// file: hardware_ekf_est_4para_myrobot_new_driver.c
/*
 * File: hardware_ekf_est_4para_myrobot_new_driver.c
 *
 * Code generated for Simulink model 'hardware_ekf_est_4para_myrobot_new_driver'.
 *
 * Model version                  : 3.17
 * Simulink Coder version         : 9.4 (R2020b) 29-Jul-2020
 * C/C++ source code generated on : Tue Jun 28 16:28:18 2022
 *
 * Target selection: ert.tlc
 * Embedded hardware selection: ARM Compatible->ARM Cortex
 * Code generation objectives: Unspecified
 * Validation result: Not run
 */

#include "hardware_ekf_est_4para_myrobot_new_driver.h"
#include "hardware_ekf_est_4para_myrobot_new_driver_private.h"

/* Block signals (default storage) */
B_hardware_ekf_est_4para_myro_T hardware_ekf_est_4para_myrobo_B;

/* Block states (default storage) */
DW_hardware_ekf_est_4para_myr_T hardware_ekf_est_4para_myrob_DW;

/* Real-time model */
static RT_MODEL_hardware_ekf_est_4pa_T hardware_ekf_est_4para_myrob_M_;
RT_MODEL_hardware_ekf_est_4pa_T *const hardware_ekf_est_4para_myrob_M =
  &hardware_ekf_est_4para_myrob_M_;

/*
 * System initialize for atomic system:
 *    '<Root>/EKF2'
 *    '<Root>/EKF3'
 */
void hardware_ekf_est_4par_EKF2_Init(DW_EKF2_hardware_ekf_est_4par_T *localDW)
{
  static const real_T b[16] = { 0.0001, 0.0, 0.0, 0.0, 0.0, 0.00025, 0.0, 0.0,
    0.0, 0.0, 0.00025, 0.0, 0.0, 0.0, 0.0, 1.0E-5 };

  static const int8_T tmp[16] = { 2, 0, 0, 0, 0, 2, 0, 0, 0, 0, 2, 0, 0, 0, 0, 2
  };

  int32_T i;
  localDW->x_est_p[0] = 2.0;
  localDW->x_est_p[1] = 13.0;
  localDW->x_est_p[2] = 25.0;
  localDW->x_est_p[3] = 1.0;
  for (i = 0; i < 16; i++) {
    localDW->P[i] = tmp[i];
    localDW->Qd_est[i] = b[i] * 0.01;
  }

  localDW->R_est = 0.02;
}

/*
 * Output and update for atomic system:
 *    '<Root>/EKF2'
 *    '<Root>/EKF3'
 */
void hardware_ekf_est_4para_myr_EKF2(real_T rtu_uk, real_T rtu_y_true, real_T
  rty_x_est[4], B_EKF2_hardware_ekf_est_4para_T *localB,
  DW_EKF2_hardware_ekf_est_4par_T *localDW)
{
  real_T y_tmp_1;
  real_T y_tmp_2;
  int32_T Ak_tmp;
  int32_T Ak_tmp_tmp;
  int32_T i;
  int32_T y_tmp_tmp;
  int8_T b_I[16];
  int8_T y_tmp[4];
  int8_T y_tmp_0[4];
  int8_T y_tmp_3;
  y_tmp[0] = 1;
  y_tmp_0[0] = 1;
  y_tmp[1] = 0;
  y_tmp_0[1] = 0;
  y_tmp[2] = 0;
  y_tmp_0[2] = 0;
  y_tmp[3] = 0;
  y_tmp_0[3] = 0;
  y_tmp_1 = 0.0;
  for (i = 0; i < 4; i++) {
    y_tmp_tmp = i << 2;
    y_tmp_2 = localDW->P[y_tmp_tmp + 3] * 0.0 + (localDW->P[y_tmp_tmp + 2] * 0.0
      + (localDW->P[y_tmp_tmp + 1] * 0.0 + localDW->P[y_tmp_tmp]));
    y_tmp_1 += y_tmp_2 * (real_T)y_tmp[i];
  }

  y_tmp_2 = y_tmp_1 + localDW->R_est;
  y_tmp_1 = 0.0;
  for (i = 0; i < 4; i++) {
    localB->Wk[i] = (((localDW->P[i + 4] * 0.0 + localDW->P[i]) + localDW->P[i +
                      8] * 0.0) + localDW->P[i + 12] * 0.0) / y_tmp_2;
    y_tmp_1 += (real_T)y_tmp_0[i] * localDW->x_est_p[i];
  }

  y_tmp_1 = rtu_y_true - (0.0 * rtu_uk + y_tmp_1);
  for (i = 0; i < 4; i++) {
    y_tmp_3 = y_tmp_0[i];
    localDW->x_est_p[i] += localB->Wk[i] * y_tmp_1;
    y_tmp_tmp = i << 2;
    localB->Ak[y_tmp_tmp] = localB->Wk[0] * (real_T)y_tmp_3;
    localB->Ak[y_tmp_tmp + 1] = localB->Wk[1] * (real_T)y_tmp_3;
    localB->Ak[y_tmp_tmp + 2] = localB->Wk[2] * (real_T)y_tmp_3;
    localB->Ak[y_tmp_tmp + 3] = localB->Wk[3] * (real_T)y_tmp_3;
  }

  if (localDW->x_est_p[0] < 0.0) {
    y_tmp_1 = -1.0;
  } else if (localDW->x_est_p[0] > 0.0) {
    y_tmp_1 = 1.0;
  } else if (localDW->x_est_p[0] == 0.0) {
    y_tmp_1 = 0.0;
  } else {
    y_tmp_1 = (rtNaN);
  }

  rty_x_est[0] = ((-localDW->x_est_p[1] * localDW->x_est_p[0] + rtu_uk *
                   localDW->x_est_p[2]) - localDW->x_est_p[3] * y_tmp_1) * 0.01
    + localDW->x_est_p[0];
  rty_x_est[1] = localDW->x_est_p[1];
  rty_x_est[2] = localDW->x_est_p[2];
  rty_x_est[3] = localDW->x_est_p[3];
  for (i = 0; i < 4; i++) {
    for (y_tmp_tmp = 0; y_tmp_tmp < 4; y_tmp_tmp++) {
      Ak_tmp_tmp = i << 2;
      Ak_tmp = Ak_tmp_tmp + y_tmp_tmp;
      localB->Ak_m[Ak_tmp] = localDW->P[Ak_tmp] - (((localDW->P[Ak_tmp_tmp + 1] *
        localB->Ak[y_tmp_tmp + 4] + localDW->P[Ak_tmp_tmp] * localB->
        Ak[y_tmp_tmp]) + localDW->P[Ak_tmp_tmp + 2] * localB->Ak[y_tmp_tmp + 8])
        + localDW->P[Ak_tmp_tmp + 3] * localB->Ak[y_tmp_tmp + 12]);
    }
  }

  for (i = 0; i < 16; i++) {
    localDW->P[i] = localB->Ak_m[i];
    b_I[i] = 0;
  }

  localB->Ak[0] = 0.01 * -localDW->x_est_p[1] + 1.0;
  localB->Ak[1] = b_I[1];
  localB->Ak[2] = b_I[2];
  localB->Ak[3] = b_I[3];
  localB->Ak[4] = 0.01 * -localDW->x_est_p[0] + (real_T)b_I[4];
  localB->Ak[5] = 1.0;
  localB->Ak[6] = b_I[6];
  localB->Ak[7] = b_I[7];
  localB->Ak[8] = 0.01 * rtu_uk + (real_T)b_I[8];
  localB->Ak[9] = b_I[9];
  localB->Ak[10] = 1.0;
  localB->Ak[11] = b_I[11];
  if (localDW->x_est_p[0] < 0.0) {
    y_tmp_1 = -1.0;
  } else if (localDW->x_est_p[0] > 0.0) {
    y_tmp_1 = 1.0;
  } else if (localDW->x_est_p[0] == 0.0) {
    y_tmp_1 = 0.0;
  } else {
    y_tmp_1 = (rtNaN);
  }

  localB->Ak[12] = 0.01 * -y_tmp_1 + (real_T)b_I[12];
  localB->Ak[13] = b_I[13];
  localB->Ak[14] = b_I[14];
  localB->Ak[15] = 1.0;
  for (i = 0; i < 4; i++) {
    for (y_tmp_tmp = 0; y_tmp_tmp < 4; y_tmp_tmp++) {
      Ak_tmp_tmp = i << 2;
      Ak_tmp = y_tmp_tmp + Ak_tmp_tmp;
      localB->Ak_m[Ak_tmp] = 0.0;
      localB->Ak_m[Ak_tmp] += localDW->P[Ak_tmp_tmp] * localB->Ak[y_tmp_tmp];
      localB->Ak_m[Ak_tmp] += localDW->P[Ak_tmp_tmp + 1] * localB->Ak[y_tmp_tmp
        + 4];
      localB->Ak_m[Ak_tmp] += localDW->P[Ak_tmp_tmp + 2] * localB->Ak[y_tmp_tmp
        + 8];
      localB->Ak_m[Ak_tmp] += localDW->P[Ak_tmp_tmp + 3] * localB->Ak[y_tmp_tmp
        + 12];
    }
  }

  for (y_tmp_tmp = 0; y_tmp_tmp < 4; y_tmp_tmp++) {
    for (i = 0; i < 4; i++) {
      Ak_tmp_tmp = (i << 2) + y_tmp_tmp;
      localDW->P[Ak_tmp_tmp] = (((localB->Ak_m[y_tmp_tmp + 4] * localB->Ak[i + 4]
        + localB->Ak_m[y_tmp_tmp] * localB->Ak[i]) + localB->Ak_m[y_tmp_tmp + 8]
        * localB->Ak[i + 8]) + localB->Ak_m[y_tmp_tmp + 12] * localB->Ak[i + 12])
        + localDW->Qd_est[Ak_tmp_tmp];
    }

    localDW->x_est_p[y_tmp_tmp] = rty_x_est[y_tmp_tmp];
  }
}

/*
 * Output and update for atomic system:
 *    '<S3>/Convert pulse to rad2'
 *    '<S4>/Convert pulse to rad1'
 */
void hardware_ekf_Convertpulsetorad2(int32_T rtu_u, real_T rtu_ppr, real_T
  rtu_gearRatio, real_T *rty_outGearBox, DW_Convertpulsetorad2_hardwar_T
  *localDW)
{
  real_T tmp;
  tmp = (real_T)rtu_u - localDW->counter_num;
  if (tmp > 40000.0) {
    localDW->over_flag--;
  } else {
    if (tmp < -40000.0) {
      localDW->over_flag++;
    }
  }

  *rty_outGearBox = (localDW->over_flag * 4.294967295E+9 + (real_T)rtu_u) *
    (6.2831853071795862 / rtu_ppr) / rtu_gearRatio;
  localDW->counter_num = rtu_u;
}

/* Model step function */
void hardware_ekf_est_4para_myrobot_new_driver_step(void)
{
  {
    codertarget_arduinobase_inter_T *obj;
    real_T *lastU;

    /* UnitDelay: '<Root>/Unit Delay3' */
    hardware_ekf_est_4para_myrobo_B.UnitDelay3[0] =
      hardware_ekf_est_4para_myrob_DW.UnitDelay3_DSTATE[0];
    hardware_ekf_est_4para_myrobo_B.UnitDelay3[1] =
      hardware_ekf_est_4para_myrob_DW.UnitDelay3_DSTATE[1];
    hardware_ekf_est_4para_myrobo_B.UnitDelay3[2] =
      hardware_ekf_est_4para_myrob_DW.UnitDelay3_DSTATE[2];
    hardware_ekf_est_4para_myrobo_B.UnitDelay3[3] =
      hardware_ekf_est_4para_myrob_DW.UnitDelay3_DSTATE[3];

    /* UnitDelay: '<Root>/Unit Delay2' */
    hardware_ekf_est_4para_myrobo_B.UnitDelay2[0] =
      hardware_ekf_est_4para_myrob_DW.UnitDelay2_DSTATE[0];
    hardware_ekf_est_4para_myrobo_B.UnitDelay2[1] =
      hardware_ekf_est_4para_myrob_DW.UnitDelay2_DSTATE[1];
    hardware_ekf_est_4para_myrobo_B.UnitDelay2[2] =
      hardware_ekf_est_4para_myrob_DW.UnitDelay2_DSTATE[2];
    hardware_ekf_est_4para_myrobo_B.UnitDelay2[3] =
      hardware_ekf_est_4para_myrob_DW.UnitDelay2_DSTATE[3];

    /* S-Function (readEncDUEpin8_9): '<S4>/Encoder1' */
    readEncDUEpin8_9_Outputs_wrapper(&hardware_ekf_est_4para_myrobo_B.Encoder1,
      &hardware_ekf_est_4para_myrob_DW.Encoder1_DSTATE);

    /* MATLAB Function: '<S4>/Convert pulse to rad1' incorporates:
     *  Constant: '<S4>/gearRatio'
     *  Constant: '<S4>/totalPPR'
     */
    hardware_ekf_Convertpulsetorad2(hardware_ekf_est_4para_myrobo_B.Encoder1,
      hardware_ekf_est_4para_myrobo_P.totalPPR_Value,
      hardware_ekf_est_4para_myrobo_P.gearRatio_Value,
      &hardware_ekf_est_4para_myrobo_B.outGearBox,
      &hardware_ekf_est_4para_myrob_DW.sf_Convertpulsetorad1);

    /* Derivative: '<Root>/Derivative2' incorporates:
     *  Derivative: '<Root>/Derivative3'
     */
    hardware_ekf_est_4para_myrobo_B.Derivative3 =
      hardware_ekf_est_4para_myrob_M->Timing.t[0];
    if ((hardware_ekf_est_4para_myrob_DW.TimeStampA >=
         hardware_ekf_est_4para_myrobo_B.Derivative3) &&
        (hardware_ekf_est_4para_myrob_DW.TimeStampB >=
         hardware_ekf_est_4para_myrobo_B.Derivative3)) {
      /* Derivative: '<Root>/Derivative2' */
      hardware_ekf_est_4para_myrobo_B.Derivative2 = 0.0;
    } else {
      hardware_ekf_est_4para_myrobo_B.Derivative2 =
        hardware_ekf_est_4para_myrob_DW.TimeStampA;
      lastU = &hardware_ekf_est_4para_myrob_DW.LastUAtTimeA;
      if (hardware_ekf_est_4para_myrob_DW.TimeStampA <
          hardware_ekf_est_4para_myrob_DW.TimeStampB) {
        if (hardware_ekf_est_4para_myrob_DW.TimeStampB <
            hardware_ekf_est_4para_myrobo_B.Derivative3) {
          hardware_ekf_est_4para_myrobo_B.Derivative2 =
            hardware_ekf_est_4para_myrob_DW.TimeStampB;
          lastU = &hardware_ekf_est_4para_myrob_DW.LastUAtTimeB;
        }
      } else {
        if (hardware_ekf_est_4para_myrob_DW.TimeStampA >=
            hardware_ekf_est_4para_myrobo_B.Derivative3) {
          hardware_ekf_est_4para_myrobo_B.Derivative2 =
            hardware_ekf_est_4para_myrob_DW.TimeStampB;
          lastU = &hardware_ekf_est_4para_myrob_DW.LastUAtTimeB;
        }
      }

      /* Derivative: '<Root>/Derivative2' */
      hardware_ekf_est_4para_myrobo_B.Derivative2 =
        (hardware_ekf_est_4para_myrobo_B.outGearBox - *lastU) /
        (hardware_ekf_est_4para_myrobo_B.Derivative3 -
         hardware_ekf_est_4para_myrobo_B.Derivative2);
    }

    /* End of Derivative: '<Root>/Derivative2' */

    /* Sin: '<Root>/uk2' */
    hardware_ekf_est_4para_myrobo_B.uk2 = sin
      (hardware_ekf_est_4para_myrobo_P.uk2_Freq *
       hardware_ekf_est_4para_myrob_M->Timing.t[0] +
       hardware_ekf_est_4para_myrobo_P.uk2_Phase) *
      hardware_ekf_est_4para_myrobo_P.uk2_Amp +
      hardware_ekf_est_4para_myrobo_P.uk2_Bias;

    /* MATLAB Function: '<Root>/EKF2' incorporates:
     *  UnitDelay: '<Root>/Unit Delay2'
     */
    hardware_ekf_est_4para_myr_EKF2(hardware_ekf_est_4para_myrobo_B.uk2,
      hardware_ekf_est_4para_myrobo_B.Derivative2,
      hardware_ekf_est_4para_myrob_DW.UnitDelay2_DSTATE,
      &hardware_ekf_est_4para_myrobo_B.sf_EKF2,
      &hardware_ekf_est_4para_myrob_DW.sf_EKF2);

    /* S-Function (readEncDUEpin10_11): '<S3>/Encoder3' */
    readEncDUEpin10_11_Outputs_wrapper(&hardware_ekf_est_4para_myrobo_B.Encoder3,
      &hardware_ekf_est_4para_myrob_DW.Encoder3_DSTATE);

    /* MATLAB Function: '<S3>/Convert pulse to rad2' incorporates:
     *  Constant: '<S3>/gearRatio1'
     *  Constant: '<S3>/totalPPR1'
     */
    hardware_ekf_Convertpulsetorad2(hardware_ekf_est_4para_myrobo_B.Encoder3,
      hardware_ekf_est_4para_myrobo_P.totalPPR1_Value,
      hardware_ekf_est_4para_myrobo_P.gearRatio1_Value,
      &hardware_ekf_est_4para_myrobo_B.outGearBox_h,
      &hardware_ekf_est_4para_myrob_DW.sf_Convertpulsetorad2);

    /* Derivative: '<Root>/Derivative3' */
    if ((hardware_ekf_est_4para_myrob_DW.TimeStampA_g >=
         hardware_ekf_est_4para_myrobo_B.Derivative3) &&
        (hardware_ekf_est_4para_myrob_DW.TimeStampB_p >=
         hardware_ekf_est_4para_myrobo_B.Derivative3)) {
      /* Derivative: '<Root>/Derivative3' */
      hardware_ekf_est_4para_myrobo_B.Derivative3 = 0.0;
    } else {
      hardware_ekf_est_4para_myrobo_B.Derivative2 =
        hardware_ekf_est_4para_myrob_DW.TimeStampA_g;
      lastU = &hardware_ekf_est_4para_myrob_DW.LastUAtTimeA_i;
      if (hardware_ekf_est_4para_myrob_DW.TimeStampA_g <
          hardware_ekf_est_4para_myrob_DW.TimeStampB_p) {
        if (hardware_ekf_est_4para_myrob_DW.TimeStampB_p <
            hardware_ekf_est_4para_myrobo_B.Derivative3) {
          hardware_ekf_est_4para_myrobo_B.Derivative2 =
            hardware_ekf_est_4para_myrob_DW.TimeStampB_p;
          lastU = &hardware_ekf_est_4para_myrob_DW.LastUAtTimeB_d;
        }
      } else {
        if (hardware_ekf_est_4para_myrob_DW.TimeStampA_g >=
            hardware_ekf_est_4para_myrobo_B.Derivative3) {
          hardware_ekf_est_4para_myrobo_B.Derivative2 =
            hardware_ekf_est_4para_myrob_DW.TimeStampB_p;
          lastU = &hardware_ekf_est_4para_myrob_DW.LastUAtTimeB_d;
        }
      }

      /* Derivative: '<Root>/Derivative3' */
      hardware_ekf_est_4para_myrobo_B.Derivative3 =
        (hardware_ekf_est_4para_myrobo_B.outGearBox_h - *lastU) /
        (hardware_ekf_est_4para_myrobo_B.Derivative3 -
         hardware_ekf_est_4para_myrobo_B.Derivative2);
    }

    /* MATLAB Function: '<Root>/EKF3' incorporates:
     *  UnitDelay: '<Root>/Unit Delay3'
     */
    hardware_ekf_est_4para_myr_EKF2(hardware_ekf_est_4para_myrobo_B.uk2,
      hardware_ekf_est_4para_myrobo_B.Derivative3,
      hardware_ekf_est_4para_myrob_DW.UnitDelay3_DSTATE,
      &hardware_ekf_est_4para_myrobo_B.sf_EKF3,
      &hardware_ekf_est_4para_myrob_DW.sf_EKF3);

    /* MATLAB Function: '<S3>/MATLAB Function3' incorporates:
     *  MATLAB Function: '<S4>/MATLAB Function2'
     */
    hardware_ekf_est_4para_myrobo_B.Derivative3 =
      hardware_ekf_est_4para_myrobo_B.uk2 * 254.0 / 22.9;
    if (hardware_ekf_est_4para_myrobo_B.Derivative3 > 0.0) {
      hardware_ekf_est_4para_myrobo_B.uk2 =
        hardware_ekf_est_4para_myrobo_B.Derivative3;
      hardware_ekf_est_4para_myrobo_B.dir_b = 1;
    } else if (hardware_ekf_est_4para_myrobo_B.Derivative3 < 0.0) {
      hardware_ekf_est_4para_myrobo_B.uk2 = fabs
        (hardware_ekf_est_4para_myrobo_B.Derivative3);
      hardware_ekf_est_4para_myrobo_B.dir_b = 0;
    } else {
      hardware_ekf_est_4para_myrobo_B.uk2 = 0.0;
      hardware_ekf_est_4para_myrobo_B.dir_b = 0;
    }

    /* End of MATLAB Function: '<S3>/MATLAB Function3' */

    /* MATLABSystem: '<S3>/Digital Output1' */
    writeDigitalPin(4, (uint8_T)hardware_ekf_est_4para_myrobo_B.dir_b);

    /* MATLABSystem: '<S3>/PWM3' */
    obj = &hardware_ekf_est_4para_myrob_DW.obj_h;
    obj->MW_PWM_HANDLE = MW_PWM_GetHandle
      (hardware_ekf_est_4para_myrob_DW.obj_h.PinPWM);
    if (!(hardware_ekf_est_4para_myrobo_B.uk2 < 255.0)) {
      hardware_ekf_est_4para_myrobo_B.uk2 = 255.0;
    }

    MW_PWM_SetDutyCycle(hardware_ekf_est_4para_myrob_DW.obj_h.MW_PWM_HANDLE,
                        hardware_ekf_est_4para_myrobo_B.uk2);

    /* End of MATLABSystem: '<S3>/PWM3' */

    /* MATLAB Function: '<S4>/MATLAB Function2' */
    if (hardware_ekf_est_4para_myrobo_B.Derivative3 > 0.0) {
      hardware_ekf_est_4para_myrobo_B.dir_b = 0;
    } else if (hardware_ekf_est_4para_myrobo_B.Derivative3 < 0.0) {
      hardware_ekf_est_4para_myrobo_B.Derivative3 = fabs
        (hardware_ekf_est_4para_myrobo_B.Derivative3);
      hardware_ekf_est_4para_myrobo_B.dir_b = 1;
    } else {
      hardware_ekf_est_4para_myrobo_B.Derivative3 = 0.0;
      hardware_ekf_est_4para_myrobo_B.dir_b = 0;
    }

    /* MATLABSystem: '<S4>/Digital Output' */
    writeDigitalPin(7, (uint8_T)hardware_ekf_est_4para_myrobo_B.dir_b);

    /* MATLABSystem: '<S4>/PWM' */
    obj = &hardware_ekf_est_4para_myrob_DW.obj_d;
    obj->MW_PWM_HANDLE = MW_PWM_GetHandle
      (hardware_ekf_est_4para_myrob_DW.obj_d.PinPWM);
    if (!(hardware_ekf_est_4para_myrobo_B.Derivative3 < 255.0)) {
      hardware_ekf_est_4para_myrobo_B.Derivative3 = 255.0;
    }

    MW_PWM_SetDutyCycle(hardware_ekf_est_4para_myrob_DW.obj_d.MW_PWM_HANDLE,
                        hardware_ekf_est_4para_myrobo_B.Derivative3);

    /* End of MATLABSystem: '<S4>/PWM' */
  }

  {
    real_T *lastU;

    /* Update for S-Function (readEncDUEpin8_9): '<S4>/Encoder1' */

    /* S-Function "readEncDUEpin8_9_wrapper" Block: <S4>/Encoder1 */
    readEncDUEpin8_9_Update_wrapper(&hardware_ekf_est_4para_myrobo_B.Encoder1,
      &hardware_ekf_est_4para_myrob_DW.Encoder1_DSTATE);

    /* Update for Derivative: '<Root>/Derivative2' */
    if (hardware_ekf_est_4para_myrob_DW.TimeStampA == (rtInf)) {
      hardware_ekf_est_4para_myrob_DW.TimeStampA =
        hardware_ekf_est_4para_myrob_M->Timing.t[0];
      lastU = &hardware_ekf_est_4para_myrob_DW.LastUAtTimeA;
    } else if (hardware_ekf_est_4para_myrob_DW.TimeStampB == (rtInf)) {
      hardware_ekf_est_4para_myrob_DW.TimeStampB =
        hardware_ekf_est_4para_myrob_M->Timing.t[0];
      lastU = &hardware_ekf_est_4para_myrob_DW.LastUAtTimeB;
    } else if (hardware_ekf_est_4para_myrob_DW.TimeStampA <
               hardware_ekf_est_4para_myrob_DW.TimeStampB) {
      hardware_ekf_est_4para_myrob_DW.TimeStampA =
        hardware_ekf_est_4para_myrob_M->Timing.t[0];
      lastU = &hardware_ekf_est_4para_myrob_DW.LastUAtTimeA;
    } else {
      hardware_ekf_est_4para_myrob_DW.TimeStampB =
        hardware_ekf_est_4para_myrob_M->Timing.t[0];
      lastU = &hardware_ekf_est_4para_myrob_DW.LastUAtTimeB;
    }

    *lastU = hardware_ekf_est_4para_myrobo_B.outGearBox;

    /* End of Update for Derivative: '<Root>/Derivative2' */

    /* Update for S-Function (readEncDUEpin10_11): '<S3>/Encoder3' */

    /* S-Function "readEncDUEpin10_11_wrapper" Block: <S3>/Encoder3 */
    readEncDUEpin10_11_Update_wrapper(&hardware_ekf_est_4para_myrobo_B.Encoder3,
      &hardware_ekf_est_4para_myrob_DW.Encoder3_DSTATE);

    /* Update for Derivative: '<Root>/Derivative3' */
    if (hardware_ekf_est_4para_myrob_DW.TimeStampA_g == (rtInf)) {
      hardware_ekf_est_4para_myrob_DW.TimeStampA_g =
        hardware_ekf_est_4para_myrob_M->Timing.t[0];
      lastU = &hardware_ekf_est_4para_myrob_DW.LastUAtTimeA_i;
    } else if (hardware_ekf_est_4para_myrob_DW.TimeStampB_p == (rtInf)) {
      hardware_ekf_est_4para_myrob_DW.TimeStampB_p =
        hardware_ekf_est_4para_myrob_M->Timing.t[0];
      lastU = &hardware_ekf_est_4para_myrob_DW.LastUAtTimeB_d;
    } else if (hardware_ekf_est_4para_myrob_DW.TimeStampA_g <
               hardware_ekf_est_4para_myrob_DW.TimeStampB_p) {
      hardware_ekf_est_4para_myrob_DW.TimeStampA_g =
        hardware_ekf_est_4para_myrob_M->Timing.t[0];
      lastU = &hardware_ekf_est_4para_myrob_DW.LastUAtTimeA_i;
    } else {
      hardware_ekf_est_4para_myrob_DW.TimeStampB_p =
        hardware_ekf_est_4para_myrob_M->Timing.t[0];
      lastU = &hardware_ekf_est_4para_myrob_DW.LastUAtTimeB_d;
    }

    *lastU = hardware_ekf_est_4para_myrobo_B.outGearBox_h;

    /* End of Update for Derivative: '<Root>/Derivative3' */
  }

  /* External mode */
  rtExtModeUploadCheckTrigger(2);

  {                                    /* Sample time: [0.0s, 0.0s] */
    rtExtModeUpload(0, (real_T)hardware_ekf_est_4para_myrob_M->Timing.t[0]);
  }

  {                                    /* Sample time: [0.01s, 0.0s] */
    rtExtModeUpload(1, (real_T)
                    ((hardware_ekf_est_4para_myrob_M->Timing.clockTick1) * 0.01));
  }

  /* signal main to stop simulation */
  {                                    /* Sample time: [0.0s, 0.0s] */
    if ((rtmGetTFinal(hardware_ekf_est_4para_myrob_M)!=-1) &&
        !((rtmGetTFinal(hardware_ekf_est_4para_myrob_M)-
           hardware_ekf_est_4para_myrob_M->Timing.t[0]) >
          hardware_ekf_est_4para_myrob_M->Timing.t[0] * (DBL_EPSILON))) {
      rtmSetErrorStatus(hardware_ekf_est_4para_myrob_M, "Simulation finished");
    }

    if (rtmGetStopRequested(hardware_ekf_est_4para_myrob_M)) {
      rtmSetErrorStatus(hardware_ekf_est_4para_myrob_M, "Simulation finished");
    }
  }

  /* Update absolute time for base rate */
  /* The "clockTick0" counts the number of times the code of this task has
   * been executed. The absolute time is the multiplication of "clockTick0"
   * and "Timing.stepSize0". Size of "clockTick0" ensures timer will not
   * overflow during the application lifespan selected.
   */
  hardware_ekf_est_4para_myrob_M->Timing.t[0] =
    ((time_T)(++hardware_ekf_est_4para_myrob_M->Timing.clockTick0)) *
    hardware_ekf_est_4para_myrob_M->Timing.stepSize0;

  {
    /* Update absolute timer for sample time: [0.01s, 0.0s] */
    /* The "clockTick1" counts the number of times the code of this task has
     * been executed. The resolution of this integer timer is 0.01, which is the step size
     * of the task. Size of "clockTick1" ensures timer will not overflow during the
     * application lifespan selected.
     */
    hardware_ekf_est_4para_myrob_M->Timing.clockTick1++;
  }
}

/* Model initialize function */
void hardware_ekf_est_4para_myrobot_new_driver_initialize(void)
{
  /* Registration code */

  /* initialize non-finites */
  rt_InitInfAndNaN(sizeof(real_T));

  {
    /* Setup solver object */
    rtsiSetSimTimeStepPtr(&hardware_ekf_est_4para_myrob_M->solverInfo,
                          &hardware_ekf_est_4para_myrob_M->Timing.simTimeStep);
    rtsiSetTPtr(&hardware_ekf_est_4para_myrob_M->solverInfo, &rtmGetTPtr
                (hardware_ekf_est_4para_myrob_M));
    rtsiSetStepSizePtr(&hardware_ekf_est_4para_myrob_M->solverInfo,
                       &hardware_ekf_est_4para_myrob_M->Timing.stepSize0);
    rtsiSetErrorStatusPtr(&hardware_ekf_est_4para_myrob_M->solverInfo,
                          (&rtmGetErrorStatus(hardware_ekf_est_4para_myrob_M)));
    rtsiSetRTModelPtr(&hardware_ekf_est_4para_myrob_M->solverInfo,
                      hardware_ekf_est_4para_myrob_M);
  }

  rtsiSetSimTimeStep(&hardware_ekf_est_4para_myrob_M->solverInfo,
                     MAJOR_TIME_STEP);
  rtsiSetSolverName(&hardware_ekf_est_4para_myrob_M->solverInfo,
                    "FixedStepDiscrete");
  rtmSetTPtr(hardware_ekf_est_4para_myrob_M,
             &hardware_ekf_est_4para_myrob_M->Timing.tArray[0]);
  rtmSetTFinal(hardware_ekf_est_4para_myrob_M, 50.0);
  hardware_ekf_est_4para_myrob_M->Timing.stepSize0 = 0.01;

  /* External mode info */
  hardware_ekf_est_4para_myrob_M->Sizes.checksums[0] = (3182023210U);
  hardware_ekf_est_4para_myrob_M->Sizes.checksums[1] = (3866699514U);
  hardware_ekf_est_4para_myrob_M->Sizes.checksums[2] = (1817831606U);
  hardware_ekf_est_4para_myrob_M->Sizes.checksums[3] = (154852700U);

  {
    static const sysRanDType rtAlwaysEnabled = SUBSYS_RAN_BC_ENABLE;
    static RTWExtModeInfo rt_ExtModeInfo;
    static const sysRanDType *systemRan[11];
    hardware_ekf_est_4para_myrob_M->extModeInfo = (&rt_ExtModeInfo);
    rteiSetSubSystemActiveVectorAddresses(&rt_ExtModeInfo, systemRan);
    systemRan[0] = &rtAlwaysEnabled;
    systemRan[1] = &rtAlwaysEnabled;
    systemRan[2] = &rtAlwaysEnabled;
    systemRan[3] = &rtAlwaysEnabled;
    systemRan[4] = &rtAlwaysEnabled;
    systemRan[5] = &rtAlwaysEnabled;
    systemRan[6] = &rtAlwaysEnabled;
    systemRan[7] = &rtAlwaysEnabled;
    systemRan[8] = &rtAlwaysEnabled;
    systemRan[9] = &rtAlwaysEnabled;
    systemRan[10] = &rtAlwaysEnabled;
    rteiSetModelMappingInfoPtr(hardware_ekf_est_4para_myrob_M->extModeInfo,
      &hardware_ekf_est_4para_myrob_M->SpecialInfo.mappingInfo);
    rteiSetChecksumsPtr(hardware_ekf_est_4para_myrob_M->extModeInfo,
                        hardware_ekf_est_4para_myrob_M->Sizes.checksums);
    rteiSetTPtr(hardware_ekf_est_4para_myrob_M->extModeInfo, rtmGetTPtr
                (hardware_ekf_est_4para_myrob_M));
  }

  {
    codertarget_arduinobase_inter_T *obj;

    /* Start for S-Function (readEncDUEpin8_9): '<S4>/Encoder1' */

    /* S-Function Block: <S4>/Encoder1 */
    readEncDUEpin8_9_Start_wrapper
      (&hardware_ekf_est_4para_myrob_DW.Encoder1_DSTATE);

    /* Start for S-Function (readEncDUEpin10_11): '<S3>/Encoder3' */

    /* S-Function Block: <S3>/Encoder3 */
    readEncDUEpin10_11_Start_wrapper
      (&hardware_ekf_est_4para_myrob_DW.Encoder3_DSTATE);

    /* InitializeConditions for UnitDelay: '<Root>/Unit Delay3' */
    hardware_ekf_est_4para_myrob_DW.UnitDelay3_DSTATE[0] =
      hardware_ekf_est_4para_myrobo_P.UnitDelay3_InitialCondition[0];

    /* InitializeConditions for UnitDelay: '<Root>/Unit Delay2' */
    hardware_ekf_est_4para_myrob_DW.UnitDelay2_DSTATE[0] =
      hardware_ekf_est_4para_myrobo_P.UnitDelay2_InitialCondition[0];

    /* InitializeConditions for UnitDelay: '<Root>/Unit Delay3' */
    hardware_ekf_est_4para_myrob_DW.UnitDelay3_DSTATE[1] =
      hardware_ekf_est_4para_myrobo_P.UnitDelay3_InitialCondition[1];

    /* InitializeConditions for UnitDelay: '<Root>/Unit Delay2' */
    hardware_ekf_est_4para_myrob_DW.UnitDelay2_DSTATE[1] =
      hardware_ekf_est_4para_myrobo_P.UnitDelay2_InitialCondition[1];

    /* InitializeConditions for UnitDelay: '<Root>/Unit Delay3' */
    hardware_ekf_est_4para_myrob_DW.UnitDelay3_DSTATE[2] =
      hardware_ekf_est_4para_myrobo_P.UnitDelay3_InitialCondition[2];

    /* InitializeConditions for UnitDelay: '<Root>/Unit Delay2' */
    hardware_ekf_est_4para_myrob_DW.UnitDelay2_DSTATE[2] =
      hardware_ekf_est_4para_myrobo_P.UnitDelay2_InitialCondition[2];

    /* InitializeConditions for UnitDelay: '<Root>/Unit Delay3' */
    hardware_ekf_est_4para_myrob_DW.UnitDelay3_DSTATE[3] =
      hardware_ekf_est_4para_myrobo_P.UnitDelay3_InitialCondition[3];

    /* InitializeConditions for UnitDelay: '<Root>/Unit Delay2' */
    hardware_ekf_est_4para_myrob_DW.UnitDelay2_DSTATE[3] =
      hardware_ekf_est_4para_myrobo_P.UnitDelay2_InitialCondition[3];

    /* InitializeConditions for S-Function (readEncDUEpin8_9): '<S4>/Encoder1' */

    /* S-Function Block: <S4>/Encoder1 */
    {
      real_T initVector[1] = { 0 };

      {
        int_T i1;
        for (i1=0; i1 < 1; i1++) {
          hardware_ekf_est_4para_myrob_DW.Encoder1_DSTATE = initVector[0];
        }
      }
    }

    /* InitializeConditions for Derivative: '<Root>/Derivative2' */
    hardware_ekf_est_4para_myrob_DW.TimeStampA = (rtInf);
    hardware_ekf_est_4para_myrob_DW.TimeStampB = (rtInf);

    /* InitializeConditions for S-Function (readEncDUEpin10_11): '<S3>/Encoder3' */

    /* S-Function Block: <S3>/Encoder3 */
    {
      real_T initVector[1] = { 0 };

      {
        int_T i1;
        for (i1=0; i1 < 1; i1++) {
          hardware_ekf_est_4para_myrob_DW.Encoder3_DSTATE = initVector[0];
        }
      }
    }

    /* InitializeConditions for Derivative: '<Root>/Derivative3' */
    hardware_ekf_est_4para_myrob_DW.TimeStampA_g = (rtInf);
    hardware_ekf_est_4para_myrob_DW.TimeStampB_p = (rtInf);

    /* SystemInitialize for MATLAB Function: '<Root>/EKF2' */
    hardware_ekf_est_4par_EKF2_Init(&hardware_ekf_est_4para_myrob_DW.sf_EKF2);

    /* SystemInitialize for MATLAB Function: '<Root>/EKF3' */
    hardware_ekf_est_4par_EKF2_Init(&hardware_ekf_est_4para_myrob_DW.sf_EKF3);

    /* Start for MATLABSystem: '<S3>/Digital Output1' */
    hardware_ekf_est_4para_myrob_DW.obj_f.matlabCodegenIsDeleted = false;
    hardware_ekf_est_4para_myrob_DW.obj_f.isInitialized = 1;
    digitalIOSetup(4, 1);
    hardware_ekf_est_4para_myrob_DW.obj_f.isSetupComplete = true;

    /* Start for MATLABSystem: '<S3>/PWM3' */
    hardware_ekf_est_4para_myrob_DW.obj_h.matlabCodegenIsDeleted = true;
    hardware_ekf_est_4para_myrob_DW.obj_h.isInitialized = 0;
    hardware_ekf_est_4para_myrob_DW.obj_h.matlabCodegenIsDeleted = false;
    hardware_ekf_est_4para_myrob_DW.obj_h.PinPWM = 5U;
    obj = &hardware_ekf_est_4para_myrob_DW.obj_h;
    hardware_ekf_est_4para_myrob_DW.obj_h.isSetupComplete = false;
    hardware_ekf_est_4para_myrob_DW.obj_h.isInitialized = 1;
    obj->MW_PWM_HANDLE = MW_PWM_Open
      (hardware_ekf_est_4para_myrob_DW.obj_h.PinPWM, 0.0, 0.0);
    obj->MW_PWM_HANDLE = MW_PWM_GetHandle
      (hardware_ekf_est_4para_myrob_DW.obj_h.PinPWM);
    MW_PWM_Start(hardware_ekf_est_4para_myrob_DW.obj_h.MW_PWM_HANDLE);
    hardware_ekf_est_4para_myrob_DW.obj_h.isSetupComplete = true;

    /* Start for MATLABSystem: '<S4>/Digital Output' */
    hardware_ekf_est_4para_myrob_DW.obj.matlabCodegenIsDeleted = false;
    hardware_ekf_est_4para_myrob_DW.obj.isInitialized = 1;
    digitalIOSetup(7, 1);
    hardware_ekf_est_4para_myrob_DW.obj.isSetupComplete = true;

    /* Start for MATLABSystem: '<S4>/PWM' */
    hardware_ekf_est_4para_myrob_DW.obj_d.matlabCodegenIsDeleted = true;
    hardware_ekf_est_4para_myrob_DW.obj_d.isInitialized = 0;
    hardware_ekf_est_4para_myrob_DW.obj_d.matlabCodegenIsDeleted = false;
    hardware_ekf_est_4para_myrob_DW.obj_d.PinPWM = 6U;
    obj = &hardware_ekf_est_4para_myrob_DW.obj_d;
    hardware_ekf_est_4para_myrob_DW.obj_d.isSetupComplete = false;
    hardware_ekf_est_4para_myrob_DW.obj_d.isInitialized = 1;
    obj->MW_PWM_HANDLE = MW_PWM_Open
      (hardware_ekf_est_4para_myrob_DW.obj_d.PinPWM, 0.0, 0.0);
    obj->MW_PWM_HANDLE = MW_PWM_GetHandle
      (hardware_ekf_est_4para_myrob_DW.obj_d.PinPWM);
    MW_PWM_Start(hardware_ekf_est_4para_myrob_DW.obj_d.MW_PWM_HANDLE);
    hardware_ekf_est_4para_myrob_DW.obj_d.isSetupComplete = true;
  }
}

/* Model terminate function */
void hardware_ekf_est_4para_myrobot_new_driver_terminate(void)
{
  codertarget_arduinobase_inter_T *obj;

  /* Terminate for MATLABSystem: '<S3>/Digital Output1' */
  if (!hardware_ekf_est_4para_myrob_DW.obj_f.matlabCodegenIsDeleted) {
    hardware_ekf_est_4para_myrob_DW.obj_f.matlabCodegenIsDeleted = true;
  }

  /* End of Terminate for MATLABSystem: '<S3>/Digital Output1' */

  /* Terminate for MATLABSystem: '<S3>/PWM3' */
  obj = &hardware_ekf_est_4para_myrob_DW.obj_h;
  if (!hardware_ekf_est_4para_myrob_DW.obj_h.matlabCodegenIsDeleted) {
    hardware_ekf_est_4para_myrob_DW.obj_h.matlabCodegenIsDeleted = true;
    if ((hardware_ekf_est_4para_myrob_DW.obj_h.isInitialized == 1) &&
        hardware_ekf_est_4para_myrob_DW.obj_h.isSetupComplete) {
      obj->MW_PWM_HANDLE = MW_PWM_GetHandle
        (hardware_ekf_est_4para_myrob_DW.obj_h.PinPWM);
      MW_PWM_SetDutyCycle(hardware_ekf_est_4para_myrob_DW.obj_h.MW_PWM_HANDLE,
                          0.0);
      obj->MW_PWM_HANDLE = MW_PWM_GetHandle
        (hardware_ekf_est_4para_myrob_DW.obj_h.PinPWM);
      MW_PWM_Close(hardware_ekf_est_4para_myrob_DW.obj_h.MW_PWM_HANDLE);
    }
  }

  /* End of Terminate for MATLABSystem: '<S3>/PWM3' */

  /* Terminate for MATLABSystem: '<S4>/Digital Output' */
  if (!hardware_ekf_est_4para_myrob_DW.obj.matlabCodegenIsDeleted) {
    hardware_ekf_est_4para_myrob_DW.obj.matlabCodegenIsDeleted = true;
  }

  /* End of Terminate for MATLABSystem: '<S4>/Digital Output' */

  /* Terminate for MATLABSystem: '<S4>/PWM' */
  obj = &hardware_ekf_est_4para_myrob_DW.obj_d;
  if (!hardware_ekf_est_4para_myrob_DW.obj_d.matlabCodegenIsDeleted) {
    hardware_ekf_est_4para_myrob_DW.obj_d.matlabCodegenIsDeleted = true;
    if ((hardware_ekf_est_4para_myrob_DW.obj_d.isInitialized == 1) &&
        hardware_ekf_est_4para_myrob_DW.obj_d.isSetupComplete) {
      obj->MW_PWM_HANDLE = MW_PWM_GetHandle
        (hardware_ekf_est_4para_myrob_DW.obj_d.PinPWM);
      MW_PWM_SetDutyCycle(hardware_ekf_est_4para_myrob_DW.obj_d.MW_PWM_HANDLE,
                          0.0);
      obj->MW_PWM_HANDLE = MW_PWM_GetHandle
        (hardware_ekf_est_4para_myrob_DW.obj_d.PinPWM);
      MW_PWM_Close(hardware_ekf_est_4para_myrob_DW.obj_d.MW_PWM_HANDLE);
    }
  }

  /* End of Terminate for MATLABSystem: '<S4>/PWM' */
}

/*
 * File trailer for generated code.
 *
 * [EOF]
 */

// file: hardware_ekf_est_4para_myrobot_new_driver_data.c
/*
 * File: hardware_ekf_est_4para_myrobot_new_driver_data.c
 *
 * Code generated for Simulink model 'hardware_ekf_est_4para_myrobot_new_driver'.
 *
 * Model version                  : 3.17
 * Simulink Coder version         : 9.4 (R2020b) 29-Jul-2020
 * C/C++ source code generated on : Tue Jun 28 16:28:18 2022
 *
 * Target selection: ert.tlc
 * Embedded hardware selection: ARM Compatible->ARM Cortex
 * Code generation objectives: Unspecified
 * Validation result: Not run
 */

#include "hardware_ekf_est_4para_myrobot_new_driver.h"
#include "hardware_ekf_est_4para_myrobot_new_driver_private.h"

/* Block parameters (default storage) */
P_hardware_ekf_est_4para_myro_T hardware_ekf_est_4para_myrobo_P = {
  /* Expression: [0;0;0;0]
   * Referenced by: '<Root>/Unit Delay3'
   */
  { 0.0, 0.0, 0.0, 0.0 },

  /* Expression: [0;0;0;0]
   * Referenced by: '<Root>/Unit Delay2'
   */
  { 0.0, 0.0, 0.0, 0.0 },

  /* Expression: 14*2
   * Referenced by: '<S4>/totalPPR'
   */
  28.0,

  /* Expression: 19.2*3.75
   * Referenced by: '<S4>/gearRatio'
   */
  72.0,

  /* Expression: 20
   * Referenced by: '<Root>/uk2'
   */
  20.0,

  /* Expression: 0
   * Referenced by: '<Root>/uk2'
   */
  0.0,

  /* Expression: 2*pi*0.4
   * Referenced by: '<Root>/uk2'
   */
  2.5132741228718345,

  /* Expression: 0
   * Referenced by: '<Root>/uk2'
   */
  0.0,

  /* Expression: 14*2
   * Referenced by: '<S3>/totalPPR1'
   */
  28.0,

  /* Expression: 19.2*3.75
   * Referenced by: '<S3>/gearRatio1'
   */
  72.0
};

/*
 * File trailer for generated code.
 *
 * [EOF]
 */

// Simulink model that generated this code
simulink model "hardware_ekf_est_4para_myrobot_new_driver"  (R2020b)
settings: Solver=ode1  StartTime=0.0  StopTime=60  FixedStep=0.01  RelTol=1e-3  EnableMultiTasking=on
libraries: arduinolib x4

== system hardware_ekf_est_4para_myrobot_new_driver ==
  Derivative2 : Derivative
  Derivative3 : Derivative
  Display2 : Display
  Display3 : Display
  EKF2 : MATLAB Function  TreatAsAtomicUnit=on
  EKF3 : MATLAB Function  TreatAsAtomicUnit=on
  Left Motor : Subsystem
  Right motor : Subsystem
  Scope2 : Scope
  Scope3 : Scope
  Unit Delay2 : UnitDelay  InitialCondition=[0;0;0;0]  SampleTime=-1  HasFrameUpgradeWarning=on
  Unit Delay3 : UnitDelay  InitialCondition=[0;0;0;0]  SampleTime=-1  HasFrameUpgradeWarning=on
  uk2 : Sin  Amplitude=20  Frequency=2*pi*0.4  SampleTime=0
  wires:
  Right motor/1(outGearBox) -> Derivative2/1
  Derivative2/1 -> EKF2/2(y_true)
  Derivative3/1 -> EKF3/2(y_true)
  uk2/1 -> Left Motor/1(v_a), EKF3/1(uk), EKF2/1(uk), Right motor/1(v_a)
  Left Motor/1(outGearBox) -> Derivative3/1
  EKF2/1(x_est) -> Unit Delay2/1
  EKF3/1(x_est) -> Unit Delay3/1
  Unit Delay3/1 -> Scope2/1, Display2/1
  Unit Delay2/1 -> Display3/1, Scope3/1

== system hardware_ekf_est_4para_myrobot_new_driver/Left Motor ==
  v_a : Inport
  Convert pulse to rad2 : MATLAB Function  TreatAsAtomicUnit=on
  Digital Output1 : arduinolib/Digital Output  pinNumber=4  Direction=output  blockPlatform=arduino
  Encoder3 : S-Function  InitFcn=try, set_param(gcb,'FunctionName','readEncDUEpin10_11'), end  FunctionName=readEncDUEpin10_11  SFunctionModules=readEncDUEpin10_11_wrapper  SFunctionDeploymentMode=off  EnableBusSupport=off  mask(S-Function Builder){}
      mask help: Simulink:masks:SFunctionBuilder_MD
      mask init:
      | val = [[.9  0.75 0.75 1 1 .9 .9 1]',[1 1 0.75 0.75 .9 .9 1 .9]'];try , sys = get_param(gcb,'SfunBuilderFcnName');if isempty(sys), sys = get_param(gcb,'FunctionName'); end,catch, sys = get_param(gcb,'FunctionName'); end
  MATLAB Function3 : MATLAB Function  TreatAsAtomicUnit=on
  PWM3 : arduinolib/PWM  pinNumber=5  frequencyType=Default  desiredFrequency=490.2  achievableFrequency=490.2
  gearRatio1 : Constant  Value=19.2*3.75
  totalPPR1 : Constant  Value=14*2
  outGearBox : Outport
  wires:
  totalPPR1/1 -> Convert pulse to rad2/2(ppr)
  Convert pulse to rad2/1(outGearBox) -> outGearBox/1
  MATLAB Function3/2(dir) -> Digital Output1/1
  MATLAB Function3/1(pwm) -> PWM3/1
  Encoder3/1 -> Convert pulse to rad2/1(u)
  v_a/1 -> MATLAB Function3/1(v_a)
  gearRatio1/1 -> Convert pulse to rad2/3(gearRatio)

== system hardware_ekf_est_4para_myrobot_new_driver/Right motor ==
  v_a : Inport
  Convert pulse to rad1 : MATLAB Function  TreatAsAtomicUnit=on
  Digital Output : arduinolib/Digital Output  pinNumber=7  Direction=output  blockPlatform=arduino
  Encoder1 : S-Function  InitFcn=try, set_param(gcb,'FunctionName','readEncDUEpin8_9'), end  FunctionName=readEncDUEpin8_9  SFunctionModules=readEncDUEpin8_9_wrapper  SFunctionDeploymentMode=off  EnableBusSupport=off  mask(S-Function Builder){}
      mask help: Simulink:masks:SFunctionBuilder_MD
      mask init: same as hardware_ekf_est_4para_myrobot_new_driver/Left Motor/Encoder3
  MATLAB Function2 : MATLAB Function  TreatAsAtomicUnit=on
  PWM : arduinolib/PWM  pinNumber=6  frequencyType=Default  desiredFrequency=490.2  achievableFrequency=490.2
  gearRatio : Constant  Value=19.2*3.75
  totalPPR : Constant  Value=14*2
  outGearBox : Outport
  wires:
  totalPPR/1 -> Convert pulse to rad1/2(ppr)
  v_a/1 -> MATLAB Function2/1(v_a)
  MATLAB Function2/2(dir) -> Digital Output/1
  MATLAB Function2/1(pwm) -> PWM/1
  gearRatio/1 -> Convert pulse to rad1/3(gearRatio)
  Convert pulse to rad1/1(outGearBox) -> outGearBox/1
  Encoder1/1 -> Convert pulse to rad1/1(u)

== matlab function hardware_ekf_est_4para_myrobot_new_driver/Left Motor/Convert pulse to rad2 ==
  settings: updateMethod=DISCRETE
function outGearBox = fcn(u,ppr,gearRatio)

persistent counter_num over_flag
if(isempty(counter_num)), counter_num = 0;end
if(isempty(over_flag)), over_flag = 0;end
pulse2radian = 2*pi/ppr; % 1 pulse = ?? radian

if(double(u) - counter_num > 40000), over_flag = over_flag-1;
elseif(double(u) - counter_num < -40000), over_flag = over_flag+1;
end

inGearBox = (double(u)+over_flag*(2^32 -1))*pulse2radian; 
outGearBox = inGearBox/gearRatio;
counter_num = double(u) ;

== matlab function hardware_ekf_est_4para_myrobot_new_driver/Right motor/MATLAB Function2 ==
function [pwm,dir] = fcn(v_a)

vmax = 22.9;
pwm_cal = v_a*254/vmax;
if pwm_cal > 0
    pwm = pwm_cal;
    dir = 0;
elseif pwm_cal < 0
    pwm = abs(pwm_cal);
    dir = 1;
else
    pwm = 0;
    dir = 0;
end

== matlab function hardware_ekf_est_4para_myrobot_new_driver/Left Motor/MATLAB Function3 ==
function [pwm,dir] = fcn(v_a)

vmax = 22.9;
pwm_cal = v_a*254/vmax;
if pwm_cal > 0
    pwm = pwm_cal;
    dir = 1;
elseif pwm_cal < 0
    pwm = abs(pwm_cal);
    dir = 0;
else
    pwm = 0;
    dir = 0;
end

== matlab function hardware_ekf_est_4para_myrobot_new_driver/EKF2 ==
  settings: updateMethod=DISCRETE
function x_est = fcn(uk,y_true)
Ts=0.01;
persistent x_est_p P Qd_est R_est Qc_est;
if isempty(x_est_p)
          
          x_est_p=[2;13;25;1];
          P=2*eye(4);
         Qc_est=1e-5*diag([10,25,25,1]);
          Qd_est=Qc_est*Ts;
          R_est=0.02;
end
c=[1 0 0 0];D=0;Ck=c;Dk=D;
%Comput Kalman Gain and update predicted value
Wk=P*Ck'/(Ck*P*Ck'+R_est);
y_est=Ck*x_est_p+Dk*uk;
x=x_est_p+Wk.*(y_true-y_est);
%Compute prediction at next time step
x_est=x+Ts*[-x(2)*x(1)+uk*x(3)-x(4)*sign(x(1));0;0;0];
%Update error covariance matrices
P=P-Wk*Ck*P;
%Define Ak
Ak=eye(4)+Ts*[-x(2) -x(1) uk -sign(x(1));0 0 0 0;0 0 0 0;0 0 0 0];
P=Ak*P*Ak'+Qd_est;
x_est_p=x_est;

== matlab function hardware_ekf_est_4para_myrobot_new_driver/EKF3 ==
  settings: updateMethod=DISCRETE
function x_est = fcn(uk,y_true)
Ts=0.01;
persistent x_est_p P Qd_est R_est Qc_est;
if isempty(x_est_p)
          
          x_est_p=[2;13;25;1];
          P=2*eye(4);
         Qc_est=1e-5*diag([10,25,25,1]);
          Qd_est=Qc_est*Ts;
          R_est=0.02;
end
c=[1 0 0 0];D=0;Ck=c;Dk=D;
%Comput Kalman Gain and update predicted value
Wk=P*Ck'/(Ck*P*Ck'+R_est);
y_est=Ck*x_est_p+Dk*uk;
x=x_est_p+Wk.*(y_true-y_est);
%Compute prediction at next time step
x_est=x+Ts*[-x(2)*x(1)+uk*x(3)-x(4)*sign(x(1));0;0;0];
%Update error covariance matrices
P=P-Wk*Ck*P;
%Define Ak
Ak=eye(4)+Ts*[-x(2) -x(1) uk -sign(x(1));0 0 0 0;0 0 0 0;0 0 0 0];
P=Ak*P*Ak'+Qd_est;
x_est_p=x_est;

== matlab function hardware_ekf_est_4para_myrobot_new_driver/Right motor/Convert pulse to rad1 ==
  settings: updateMethod=DISCRETE
function outGearBox = fcn(u,ppr,gearRatio)

persistent counter_num over_flag
if(isempty(counter_num)), counter_num = 0;end
if(isempty(over_flag)), over_flag = 0;end
pulse2radian = 2*pi/ppr; % 1 pulse = ?? radian

if(double(u) - counter_num > 40000), over_flag = over_flag-1;
elseif(double(u) - counter_num < -40000), over_flag = over_flag+1;
end

inGearBox = (double(u)+over_flag*(2^32 -1))*pulse2radian; 
outGearBox = inGearBox/gearRatio;
counter_num = double(u) ;
